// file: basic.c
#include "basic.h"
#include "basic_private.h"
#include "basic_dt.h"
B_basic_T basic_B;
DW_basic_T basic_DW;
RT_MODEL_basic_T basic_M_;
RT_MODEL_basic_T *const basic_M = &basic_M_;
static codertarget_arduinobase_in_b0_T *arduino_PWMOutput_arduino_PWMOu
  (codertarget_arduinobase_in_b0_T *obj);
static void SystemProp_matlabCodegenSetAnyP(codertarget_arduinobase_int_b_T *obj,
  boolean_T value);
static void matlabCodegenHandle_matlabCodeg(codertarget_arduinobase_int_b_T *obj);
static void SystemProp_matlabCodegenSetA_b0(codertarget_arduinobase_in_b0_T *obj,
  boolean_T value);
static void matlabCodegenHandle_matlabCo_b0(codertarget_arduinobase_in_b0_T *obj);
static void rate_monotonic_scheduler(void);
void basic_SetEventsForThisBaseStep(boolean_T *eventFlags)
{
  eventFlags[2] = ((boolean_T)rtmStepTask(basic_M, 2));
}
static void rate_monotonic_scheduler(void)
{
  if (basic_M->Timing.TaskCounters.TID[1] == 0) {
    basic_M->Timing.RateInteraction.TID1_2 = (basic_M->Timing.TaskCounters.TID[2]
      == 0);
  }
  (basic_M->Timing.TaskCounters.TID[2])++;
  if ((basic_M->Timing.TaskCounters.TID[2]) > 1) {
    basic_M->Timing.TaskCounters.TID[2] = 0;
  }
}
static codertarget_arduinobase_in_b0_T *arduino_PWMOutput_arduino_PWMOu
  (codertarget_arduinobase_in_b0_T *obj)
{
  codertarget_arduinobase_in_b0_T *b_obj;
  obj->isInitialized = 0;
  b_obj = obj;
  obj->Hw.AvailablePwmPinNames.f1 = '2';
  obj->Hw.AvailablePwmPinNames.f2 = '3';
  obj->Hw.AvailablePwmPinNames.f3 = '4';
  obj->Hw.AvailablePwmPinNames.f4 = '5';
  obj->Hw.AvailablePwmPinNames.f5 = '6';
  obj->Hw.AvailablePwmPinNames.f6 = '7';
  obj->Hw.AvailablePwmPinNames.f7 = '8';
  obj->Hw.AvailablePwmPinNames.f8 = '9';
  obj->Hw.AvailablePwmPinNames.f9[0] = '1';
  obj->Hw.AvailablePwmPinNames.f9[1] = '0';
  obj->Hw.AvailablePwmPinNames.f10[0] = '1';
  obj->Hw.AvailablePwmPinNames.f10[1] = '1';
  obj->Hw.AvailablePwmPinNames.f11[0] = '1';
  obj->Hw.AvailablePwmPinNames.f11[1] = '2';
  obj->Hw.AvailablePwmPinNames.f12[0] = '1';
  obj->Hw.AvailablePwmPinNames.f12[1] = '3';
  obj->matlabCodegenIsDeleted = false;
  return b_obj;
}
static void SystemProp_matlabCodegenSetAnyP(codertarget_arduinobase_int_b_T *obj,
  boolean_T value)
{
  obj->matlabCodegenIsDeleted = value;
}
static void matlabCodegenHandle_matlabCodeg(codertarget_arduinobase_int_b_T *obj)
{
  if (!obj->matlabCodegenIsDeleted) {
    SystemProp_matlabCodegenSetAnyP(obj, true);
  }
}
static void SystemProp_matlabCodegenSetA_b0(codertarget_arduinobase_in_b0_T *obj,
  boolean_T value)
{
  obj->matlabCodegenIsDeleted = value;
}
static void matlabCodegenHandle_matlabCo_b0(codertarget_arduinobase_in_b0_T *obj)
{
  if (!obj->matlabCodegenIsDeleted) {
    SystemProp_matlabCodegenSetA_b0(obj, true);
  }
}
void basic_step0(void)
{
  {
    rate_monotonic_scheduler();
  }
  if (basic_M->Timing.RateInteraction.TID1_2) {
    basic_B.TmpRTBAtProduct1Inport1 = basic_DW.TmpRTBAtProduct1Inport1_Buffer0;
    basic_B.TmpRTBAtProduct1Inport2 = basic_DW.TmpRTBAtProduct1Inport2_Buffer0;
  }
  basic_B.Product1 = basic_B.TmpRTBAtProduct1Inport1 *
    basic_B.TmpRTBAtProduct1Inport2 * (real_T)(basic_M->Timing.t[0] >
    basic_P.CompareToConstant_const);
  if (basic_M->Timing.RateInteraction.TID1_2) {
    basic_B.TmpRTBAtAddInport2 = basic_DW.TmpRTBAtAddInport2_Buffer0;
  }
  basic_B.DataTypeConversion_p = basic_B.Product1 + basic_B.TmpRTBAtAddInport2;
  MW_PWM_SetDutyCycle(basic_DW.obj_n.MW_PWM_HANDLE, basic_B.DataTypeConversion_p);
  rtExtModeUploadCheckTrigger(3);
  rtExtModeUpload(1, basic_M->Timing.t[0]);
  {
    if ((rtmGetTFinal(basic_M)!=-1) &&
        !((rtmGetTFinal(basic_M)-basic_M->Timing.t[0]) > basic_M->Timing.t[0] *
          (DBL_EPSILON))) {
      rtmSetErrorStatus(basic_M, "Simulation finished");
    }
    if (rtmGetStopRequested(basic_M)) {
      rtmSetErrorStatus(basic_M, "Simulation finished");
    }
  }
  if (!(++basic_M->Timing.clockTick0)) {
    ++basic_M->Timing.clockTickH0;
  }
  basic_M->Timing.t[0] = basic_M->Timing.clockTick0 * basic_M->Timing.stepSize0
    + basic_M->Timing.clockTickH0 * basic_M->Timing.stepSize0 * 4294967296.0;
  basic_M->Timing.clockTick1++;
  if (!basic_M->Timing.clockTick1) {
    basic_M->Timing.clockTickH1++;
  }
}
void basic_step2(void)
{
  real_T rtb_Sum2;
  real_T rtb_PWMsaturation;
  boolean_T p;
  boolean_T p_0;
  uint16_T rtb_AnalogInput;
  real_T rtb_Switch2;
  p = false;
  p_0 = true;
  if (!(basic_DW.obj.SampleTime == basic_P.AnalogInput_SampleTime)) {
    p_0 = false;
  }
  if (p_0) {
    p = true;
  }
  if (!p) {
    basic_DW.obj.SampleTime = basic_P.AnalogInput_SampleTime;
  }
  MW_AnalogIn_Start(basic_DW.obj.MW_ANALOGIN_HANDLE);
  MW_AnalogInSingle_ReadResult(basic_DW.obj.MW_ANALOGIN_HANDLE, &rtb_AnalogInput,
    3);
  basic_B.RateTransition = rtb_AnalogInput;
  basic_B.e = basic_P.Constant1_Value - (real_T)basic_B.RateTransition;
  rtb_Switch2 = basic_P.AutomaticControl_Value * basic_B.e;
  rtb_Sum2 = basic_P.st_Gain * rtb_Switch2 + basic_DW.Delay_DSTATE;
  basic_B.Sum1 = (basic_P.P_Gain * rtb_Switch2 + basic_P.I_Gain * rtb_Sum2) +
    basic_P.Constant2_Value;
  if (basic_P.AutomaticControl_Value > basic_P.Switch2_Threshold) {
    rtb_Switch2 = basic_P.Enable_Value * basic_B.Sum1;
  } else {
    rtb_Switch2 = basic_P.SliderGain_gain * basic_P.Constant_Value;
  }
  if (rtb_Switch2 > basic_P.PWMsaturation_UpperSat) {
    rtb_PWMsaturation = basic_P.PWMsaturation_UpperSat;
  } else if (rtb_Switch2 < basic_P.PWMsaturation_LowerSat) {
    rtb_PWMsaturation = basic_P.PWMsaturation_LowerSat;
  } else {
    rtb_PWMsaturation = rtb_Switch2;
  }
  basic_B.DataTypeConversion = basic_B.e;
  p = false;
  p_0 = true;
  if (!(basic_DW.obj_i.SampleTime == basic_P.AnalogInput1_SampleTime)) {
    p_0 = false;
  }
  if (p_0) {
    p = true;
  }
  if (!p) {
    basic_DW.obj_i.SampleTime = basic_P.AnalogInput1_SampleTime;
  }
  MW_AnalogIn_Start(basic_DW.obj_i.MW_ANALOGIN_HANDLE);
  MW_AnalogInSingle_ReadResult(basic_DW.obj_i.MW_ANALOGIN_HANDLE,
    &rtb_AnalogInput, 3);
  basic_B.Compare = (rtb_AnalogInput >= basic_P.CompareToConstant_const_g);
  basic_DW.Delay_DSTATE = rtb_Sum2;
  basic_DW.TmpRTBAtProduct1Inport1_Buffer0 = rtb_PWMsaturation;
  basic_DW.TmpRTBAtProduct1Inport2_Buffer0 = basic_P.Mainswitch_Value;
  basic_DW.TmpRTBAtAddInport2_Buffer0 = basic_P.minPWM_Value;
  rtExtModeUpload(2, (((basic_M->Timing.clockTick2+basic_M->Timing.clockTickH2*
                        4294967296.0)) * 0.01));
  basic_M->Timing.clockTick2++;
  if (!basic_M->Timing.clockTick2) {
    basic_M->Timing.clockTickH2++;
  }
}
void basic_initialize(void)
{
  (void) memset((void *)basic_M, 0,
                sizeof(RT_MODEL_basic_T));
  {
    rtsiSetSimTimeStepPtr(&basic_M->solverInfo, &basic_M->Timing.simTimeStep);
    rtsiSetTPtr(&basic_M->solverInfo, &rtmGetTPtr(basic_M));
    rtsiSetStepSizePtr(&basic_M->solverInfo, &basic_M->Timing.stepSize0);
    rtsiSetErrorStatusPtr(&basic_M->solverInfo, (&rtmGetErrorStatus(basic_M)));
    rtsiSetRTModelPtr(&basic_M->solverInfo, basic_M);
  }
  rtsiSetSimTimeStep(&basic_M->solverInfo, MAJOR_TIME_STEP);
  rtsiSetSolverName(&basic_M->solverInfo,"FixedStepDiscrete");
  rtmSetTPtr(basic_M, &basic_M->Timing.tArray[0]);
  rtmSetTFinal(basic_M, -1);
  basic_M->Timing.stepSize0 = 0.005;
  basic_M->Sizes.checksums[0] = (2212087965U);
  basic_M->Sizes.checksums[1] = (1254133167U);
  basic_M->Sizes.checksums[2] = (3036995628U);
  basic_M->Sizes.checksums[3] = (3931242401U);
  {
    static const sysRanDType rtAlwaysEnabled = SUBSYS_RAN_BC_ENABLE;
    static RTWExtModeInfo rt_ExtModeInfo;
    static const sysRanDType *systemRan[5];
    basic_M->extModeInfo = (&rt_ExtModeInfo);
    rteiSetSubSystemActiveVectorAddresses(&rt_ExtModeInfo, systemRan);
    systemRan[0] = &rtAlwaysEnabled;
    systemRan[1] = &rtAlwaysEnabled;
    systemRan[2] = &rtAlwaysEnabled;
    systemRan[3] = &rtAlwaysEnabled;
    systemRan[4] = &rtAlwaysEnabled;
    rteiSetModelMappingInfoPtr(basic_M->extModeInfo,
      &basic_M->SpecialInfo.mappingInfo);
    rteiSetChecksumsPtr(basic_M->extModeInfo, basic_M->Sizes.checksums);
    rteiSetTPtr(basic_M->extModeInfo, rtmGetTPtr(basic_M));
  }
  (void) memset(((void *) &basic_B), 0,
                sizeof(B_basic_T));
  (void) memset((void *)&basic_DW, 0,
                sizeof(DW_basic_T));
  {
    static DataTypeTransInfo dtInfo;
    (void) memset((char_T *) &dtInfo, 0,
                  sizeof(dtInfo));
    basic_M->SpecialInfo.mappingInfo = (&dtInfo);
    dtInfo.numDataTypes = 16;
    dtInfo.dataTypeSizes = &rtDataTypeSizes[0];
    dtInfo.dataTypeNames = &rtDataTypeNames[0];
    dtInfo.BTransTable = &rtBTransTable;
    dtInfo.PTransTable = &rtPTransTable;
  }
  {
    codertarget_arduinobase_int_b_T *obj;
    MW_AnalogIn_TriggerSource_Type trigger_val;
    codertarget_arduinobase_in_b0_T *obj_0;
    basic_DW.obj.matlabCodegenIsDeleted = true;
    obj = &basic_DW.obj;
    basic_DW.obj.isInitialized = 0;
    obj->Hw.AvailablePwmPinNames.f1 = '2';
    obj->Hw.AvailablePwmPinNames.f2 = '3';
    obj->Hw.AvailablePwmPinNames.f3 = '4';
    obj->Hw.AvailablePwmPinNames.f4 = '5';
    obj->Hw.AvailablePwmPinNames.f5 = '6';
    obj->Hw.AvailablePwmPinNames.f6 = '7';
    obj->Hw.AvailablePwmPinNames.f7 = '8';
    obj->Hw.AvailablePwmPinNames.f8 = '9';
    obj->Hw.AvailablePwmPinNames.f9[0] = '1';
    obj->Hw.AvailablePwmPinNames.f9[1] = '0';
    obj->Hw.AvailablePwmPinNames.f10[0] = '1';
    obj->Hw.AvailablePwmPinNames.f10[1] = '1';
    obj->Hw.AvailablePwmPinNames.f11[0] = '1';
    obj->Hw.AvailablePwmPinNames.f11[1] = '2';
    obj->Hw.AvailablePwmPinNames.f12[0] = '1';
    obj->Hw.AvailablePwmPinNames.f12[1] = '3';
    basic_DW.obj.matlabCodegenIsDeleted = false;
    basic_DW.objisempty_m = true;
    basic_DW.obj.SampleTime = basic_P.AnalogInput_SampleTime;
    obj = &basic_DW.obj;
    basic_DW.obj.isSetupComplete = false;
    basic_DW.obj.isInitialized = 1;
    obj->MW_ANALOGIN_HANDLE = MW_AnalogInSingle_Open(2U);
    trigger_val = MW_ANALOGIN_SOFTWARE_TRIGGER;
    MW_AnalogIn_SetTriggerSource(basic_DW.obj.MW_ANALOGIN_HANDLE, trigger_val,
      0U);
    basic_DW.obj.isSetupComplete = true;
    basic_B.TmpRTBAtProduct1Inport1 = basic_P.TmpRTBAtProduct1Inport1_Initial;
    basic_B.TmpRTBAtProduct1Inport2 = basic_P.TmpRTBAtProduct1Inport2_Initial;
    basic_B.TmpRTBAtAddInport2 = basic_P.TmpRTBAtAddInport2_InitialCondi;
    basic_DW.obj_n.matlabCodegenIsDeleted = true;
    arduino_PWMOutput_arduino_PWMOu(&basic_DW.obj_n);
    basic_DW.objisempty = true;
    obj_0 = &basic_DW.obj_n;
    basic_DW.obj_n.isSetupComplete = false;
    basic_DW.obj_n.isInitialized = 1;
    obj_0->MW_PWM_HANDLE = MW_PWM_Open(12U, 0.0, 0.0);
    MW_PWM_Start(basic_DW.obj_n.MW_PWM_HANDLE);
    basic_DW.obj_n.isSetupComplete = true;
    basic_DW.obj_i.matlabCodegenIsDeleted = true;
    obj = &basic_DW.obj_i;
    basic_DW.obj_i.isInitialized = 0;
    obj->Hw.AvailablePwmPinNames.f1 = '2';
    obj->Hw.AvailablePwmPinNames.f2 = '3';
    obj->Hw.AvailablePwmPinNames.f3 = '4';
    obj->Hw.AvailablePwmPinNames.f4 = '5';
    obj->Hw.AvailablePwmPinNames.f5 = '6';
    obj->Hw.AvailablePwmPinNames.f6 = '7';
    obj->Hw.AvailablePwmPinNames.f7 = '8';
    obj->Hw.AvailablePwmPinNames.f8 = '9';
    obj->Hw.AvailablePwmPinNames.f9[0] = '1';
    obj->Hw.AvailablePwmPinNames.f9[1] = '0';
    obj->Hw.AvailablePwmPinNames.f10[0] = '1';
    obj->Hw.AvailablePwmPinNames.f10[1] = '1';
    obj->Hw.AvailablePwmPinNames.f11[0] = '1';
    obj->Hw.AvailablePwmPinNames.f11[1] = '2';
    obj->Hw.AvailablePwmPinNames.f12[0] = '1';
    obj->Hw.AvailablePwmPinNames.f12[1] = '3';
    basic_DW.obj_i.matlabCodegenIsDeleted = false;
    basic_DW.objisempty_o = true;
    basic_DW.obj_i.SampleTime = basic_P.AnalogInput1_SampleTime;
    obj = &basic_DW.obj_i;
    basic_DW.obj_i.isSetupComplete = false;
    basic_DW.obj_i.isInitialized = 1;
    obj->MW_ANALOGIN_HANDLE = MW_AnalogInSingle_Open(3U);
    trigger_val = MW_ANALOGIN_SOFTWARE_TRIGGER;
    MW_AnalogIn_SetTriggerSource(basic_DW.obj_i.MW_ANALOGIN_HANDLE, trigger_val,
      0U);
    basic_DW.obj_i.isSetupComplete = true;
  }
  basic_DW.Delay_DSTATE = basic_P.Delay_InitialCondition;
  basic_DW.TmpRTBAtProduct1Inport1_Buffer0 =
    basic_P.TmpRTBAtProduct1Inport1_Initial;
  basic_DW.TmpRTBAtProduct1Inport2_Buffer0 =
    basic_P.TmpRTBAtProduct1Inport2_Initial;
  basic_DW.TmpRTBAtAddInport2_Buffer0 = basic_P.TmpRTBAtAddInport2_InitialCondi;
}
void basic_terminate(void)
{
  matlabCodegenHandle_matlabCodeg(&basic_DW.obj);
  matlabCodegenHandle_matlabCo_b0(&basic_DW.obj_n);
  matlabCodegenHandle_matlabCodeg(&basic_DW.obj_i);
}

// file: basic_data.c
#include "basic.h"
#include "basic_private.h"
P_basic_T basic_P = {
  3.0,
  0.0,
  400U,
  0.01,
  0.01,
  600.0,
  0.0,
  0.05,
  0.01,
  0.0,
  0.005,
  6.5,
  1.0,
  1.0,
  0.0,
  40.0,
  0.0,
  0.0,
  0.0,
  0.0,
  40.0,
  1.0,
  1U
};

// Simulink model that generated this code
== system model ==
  PWM#1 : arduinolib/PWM  pinNumber=12  <- 1: Sum#1
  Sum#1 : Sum  <- 1: Product1, 2: minPWM
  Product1 : Product  Inputs=3  <- 1: PWMsaturation, 2: Mainswitch, 3: CompareToConstant
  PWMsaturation : Saturate  UpperLimit=40  LowerLimit=0  <- 1: Switch2
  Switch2 : Switch  Criteria=u2 > Threshold  <- 1: Product#1, 2: AutomaticControl, 3: SliderGain
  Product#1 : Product  <- 1: Enable, 2: Sum1
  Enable : Constant
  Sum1 : Sum  Inputs=++  <- 1: Sum#2, 2: Constant2
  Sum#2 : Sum  Inputs=++  <- 1: Gain#1, 2: Gain#2
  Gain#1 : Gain  Gain=0.05  <- 1: Product#2
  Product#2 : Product  <- 1: AutomaticControl, 2: Sum#3
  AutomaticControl : Constant
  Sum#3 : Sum  Inputs=+-  <- 1: Constant1, 2: RateTransition
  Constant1 : Constant  Value=600
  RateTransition : RateTransition  <- 1: AnalogInput
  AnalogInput : arduinolib/Analog Input  pinNumber=2
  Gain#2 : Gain  Gain=0.005  <- 1: Sum2
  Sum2 : Sum  Inputs=++  <- 1: st, 2: Delay
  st : Gain  Gain=0.01  <- 1: Product#2
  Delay : Delay  DelayLength=1  <- 1: Sum2
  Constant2 : Constant  Value=6.5
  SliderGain : simulink/Math Operations/Slider Gain  <- 1: Constant
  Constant : Constant
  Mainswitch : Constant
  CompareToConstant : simulink/Logic and Bit Operations/Compare To Constant  relop=>  const=3  <- 1: Clock#1
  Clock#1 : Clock
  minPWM : Constant  Value=40
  CompareToConstant#1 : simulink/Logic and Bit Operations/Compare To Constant  relop=>=  const=400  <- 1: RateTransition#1
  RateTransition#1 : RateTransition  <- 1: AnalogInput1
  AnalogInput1 : arduinolib/Analog Input  pinNumber=3
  DataTypeConversion : DataTypeConversion  <- 1: Sum#3
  DataTypeConversion#1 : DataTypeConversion  <- 1: Sum#1
